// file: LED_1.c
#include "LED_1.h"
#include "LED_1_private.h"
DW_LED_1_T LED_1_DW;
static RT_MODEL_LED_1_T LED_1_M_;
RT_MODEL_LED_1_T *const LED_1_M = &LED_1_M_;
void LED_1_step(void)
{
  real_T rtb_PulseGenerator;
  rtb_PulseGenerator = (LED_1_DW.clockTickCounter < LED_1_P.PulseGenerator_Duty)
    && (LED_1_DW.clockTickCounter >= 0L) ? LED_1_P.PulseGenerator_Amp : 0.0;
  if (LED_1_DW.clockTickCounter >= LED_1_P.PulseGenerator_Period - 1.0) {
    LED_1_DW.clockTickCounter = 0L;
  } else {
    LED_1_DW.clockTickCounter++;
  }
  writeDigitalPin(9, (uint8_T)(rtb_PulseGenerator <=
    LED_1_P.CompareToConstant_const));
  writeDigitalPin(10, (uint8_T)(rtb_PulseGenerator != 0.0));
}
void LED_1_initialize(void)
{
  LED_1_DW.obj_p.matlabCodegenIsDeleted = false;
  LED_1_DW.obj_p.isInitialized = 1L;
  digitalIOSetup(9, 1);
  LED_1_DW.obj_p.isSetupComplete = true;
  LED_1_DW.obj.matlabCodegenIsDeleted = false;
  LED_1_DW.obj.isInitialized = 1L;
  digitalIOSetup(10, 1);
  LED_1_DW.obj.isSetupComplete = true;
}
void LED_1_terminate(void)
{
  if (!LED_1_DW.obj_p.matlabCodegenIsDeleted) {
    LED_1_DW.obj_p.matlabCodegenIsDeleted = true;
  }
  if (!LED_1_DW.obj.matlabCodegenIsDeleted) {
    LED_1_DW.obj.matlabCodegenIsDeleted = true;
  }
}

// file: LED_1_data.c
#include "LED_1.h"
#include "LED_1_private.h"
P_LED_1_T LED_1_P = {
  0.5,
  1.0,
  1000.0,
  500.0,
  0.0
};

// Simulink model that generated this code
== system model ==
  DigitalOutput#1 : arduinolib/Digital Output  pinNumber=9  <- 1: CompareToConstant
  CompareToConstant : simulink/Logic and Bit Operations/Compare To Constant  relop=<=  const=0.5  <- 1: PulseGenerator
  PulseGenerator : DiscretePulseGenerator  Period=1000  PulseWidth=500
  DigitalOutput#2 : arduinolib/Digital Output  pinNumber=10  <- 1: DataTypeConversion#1
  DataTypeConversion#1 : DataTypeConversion  <- 1: PulseGenerator
